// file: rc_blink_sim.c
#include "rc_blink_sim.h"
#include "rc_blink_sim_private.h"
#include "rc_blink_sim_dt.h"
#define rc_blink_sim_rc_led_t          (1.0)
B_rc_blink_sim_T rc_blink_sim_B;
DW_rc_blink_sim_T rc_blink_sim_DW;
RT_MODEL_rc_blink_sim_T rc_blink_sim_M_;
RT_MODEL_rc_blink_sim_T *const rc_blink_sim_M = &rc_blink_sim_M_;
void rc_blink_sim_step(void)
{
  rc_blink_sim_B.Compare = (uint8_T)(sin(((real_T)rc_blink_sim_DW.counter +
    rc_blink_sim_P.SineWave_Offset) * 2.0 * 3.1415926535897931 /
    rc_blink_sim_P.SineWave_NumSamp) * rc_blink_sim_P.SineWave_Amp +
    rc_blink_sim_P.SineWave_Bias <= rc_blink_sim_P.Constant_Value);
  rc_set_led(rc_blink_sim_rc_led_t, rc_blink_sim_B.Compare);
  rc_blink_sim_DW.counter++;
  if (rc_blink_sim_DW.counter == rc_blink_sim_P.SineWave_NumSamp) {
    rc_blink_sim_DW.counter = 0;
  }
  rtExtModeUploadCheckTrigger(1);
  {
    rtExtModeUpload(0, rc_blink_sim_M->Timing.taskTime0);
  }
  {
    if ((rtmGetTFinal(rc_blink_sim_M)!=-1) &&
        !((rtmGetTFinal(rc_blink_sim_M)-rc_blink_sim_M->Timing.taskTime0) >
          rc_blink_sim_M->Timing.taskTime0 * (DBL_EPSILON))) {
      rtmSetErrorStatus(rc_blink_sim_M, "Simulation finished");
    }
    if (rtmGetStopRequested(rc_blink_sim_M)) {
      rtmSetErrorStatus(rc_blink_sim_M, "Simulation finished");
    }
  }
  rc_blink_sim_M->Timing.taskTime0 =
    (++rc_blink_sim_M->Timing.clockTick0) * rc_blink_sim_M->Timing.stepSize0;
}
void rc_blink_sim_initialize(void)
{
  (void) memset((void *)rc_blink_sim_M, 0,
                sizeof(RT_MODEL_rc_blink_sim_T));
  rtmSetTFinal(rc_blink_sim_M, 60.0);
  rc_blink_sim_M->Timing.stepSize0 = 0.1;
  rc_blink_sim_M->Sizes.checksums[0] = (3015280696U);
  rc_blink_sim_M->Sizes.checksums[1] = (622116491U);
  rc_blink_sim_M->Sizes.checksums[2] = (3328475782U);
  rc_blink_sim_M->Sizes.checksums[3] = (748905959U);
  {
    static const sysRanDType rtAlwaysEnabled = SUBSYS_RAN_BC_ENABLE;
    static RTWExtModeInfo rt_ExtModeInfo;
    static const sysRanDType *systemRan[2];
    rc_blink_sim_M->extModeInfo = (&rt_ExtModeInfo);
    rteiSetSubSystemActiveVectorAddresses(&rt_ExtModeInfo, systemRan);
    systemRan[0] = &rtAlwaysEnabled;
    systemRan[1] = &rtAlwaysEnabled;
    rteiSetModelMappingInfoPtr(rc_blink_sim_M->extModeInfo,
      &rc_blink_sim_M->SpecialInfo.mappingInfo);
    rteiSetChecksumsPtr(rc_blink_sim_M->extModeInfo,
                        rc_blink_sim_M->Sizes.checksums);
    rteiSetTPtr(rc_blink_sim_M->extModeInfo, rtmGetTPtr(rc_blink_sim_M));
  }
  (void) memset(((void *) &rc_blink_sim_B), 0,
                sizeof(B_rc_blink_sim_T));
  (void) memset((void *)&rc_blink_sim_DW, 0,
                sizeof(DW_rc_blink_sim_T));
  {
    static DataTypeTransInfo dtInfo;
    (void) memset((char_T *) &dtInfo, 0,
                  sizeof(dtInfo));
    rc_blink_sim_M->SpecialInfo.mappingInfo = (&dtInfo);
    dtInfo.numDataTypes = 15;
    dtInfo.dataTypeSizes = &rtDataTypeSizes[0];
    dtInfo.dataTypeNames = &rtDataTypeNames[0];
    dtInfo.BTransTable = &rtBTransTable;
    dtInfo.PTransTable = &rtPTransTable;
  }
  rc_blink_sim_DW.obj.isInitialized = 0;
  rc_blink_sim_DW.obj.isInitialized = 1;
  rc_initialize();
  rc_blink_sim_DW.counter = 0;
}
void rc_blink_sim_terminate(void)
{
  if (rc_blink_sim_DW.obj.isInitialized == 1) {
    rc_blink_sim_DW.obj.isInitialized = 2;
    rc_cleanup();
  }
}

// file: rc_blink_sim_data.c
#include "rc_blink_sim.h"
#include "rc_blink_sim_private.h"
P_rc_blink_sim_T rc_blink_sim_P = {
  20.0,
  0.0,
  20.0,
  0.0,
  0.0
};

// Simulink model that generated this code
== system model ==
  MATLABSystem#1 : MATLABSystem  <- 1: CompareToZero#1
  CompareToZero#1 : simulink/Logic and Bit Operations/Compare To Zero  relop=<=  <- 1: SineWave
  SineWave : Sin  Amplitude=20  Frequency=2
